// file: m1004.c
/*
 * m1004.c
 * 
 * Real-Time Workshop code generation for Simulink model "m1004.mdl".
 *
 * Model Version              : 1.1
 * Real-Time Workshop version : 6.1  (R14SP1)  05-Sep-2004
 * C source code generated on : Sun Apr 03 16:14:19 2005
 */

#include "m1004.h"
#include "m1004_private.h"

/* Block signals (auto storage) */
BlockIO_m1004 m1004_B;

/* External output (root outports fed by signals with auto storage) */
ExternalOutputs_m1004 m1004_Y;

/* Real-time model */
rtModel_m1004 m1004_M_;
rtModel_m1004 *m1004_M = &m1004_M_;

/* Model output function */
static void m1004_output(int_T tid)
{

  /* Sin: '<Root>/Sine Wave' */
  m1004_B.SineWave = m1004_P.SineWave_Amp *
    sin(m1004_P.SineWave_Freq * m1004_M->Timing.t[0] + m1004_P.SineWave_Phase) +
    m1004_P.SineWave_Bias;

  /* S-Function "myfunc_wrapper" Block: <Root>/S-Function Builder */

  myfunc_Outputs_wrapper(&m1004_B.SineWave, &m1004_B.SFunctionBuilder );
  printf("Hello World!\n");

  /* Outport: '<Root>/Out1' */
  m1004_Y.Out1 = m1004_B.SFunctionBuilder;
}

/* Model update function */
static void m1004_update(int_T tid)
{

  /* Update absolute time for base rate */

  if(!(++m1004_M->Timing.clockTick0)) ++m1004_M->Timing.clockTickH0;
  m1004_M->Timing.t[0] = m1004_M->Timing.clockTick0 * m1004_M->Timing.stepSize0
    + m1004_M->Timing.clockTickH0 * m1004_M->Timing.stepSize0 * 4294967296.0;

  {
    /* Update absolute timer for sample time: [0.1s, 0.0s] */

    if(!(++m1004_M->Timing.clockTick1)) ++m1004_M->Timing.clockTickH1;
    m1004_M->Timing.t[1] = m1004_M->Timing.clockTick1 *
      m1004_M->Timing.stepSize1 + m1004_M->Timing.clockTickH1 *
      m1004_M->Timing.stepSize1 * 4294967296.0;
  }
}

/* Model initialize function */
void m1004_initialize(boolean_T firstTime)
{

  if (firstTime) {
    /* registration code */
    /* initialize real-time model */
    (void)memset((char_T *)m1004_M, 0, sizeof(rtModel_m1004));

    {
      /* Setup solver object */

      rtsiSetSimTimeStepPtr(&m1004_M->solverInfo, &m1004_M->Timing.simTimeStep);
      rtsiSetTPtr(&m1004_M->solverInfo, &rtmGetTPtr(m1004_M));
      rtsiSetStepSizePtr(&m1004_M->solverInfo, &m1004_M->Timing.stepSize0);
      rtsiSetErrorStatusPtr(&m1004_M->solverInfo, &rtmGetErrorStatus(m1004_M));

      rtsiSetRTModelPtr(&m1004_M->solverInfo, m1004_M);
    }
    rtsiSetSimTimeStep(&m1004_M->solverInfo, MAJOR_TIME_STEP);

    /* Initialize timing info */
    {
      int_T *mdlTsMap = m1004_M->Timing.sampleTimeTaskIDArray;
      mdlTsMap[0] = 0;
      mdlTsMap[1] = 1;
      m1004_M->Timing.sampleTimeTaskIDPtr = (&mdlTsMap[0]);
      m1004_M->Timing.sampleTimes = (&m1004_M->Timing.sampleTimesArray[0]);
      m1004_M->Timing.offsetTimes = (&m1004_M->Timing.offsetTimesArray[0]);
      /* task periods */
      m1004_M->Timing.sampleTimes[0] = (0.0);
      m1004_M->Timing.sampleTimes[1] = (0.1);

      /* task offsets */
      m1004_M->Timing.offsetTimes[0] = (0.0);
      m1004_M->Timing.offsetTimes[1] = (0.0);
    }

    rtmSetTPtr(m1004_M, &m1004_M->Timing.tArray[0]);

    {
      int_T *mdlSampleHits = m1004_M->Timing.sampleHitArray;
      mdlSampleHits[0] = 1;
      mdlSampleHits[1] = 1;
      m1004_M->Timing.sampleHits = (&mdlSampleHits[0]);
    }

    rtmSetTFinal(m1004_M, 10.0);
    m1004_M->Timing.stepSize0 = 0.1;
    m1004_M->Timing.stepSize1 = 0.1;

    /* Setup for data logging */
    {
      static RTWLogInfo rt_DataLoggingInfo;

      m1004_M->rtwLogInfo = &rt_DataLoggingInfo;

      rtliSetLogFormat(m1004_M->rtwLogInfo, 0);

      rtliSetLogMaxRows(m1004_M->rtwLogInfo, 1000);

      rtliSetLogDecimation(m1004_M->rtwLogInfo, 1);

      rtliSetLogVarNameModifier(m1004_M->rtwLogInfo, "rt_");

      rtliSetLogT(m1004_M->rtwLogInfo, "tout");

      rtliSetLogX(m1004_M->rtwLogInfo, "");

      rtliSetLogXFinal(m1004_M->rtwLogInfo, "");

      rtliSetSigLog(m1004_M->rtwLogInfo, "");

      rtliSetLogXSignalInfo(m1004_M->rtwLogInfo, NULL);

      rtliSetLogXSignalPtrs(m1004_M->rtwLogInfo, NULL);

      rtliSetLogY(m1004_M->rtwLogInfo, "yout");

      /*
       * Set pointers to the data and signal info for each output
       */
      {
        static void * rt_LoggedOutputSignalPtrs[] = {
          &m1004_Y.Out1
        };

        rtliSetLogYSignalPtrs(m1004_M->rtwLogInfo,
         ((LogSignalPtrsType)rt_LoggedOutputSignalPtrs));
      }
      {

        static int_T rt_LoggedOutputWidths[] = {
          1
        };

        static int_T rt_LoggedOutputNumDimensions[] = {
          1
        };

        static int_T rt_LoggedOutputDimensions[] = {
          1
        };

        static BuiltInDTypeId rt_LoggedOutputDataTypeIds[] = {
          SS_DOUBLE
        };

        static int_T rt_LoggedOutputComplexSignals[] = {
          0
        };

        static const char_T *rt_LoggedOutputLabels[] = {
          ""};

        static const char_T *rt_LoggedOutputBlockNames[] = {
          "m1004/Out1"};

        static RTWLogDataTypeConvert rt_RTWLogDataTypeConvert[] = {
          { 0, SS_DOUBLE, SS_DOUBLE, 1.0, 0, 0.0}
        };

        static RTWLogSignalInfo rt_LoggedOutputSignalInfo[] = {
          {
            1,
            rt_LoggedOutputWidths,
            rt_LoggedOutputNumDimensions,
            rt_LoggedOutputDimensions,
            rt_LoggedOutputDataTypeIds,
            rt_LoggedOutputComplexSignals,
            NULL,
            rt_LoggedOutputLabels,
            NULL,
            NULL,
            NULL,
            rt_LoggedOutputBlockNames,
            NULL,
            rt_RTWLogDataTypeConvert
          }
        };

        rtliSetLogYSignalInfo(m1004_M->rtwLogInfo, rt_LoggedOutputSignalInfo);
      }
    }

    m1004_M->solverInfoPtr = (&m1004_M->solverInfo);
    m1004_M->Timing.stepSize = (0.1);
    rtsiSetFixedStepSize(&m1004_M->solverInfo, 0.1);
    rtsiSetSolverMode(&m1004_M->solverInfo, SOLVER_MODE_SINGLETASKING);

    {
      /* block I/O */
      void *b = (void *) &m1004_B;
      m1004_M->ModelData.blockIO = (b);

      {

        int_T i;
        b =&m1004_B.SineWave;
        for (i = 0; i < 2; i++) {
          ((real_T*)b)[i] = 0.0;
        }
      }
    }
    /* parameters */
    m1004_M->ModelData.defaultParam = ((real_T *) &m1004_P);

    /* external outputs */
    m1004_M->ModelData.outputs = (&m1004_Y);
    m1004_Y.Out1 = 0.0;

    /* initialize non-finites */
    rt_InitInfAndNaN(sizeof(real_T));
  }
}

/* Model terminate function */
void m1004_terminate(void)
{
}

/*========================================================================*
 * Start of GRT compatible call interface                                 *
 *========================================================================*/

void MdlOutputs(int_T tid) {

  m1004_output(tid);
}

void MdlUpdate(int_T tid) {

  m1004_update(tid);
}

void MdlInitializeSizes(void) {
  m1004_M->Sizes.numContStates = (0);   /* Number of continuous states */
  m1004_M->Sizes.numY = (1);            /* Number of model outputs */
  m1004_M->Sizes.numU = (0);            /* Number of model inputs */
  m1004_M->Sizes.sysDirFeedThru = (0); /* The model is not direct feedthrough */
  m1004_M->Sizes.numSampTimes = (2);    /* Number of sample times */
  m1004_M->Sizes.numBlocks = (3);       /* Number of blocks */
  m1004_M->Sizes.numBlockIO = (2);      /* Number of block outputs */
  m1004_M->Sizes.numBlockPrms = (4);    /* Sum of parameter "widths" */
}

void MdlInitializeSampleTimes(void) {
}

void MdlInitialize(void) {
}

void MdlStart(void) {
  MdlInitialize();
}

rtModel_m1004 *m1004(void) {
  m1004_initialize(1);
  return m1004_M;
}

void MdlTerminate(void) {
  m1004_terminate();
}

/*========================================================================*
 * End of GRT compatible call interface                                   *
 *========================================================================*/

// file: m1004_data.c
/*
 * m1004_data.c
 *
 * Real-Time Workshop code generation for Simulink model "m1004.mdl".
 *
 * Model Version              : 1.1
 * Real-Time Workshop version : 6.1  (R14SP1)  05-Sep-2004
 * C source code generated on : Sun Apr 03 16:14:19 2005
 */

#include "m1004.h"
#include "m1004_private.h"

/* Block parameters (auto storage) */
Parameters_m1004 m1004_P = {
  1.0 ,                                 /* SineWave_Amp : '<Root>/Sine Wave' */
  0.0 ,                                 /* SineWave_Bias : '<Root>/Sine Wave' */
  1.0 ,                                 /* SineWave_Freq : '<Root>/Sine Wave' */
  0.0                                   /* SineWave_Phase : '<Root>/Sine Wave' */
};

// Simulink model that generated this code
simulink model "m1004"  (Simulink 6.1)
settings: Solver=FixedStepDiscrete  StartTime=0.0  StopTime=10.0  FixedStep=0.1  RelTol=1e-3

== system m1004 ==
  S-Function Builder : S-Function  FunctionName=myfunc  SFunctionModules=myfunc_wrapper  WizardData=DataTag0  mask(S-Function Builder){}
      mask init:
      | val = [[.9  0.75 0.75 1 1 .9 .9 1]',[1 1 0.75 0.75 .9 .9 1 .9]'];try , sys = get_param(gcb,'SfunBuilderFcnName');if isempty(sys), sys = get_param(gcb,'FunctionName'); end,catch, sys = get_param(gcb,'FunctionName'); end
  Sine Wave : Sin  SampleTime=0
  Out1 : Outport
  wires:
  Sine Wave/1 -> S-Function Builder/1
  S-Function Builder/1 -> Out1/1
